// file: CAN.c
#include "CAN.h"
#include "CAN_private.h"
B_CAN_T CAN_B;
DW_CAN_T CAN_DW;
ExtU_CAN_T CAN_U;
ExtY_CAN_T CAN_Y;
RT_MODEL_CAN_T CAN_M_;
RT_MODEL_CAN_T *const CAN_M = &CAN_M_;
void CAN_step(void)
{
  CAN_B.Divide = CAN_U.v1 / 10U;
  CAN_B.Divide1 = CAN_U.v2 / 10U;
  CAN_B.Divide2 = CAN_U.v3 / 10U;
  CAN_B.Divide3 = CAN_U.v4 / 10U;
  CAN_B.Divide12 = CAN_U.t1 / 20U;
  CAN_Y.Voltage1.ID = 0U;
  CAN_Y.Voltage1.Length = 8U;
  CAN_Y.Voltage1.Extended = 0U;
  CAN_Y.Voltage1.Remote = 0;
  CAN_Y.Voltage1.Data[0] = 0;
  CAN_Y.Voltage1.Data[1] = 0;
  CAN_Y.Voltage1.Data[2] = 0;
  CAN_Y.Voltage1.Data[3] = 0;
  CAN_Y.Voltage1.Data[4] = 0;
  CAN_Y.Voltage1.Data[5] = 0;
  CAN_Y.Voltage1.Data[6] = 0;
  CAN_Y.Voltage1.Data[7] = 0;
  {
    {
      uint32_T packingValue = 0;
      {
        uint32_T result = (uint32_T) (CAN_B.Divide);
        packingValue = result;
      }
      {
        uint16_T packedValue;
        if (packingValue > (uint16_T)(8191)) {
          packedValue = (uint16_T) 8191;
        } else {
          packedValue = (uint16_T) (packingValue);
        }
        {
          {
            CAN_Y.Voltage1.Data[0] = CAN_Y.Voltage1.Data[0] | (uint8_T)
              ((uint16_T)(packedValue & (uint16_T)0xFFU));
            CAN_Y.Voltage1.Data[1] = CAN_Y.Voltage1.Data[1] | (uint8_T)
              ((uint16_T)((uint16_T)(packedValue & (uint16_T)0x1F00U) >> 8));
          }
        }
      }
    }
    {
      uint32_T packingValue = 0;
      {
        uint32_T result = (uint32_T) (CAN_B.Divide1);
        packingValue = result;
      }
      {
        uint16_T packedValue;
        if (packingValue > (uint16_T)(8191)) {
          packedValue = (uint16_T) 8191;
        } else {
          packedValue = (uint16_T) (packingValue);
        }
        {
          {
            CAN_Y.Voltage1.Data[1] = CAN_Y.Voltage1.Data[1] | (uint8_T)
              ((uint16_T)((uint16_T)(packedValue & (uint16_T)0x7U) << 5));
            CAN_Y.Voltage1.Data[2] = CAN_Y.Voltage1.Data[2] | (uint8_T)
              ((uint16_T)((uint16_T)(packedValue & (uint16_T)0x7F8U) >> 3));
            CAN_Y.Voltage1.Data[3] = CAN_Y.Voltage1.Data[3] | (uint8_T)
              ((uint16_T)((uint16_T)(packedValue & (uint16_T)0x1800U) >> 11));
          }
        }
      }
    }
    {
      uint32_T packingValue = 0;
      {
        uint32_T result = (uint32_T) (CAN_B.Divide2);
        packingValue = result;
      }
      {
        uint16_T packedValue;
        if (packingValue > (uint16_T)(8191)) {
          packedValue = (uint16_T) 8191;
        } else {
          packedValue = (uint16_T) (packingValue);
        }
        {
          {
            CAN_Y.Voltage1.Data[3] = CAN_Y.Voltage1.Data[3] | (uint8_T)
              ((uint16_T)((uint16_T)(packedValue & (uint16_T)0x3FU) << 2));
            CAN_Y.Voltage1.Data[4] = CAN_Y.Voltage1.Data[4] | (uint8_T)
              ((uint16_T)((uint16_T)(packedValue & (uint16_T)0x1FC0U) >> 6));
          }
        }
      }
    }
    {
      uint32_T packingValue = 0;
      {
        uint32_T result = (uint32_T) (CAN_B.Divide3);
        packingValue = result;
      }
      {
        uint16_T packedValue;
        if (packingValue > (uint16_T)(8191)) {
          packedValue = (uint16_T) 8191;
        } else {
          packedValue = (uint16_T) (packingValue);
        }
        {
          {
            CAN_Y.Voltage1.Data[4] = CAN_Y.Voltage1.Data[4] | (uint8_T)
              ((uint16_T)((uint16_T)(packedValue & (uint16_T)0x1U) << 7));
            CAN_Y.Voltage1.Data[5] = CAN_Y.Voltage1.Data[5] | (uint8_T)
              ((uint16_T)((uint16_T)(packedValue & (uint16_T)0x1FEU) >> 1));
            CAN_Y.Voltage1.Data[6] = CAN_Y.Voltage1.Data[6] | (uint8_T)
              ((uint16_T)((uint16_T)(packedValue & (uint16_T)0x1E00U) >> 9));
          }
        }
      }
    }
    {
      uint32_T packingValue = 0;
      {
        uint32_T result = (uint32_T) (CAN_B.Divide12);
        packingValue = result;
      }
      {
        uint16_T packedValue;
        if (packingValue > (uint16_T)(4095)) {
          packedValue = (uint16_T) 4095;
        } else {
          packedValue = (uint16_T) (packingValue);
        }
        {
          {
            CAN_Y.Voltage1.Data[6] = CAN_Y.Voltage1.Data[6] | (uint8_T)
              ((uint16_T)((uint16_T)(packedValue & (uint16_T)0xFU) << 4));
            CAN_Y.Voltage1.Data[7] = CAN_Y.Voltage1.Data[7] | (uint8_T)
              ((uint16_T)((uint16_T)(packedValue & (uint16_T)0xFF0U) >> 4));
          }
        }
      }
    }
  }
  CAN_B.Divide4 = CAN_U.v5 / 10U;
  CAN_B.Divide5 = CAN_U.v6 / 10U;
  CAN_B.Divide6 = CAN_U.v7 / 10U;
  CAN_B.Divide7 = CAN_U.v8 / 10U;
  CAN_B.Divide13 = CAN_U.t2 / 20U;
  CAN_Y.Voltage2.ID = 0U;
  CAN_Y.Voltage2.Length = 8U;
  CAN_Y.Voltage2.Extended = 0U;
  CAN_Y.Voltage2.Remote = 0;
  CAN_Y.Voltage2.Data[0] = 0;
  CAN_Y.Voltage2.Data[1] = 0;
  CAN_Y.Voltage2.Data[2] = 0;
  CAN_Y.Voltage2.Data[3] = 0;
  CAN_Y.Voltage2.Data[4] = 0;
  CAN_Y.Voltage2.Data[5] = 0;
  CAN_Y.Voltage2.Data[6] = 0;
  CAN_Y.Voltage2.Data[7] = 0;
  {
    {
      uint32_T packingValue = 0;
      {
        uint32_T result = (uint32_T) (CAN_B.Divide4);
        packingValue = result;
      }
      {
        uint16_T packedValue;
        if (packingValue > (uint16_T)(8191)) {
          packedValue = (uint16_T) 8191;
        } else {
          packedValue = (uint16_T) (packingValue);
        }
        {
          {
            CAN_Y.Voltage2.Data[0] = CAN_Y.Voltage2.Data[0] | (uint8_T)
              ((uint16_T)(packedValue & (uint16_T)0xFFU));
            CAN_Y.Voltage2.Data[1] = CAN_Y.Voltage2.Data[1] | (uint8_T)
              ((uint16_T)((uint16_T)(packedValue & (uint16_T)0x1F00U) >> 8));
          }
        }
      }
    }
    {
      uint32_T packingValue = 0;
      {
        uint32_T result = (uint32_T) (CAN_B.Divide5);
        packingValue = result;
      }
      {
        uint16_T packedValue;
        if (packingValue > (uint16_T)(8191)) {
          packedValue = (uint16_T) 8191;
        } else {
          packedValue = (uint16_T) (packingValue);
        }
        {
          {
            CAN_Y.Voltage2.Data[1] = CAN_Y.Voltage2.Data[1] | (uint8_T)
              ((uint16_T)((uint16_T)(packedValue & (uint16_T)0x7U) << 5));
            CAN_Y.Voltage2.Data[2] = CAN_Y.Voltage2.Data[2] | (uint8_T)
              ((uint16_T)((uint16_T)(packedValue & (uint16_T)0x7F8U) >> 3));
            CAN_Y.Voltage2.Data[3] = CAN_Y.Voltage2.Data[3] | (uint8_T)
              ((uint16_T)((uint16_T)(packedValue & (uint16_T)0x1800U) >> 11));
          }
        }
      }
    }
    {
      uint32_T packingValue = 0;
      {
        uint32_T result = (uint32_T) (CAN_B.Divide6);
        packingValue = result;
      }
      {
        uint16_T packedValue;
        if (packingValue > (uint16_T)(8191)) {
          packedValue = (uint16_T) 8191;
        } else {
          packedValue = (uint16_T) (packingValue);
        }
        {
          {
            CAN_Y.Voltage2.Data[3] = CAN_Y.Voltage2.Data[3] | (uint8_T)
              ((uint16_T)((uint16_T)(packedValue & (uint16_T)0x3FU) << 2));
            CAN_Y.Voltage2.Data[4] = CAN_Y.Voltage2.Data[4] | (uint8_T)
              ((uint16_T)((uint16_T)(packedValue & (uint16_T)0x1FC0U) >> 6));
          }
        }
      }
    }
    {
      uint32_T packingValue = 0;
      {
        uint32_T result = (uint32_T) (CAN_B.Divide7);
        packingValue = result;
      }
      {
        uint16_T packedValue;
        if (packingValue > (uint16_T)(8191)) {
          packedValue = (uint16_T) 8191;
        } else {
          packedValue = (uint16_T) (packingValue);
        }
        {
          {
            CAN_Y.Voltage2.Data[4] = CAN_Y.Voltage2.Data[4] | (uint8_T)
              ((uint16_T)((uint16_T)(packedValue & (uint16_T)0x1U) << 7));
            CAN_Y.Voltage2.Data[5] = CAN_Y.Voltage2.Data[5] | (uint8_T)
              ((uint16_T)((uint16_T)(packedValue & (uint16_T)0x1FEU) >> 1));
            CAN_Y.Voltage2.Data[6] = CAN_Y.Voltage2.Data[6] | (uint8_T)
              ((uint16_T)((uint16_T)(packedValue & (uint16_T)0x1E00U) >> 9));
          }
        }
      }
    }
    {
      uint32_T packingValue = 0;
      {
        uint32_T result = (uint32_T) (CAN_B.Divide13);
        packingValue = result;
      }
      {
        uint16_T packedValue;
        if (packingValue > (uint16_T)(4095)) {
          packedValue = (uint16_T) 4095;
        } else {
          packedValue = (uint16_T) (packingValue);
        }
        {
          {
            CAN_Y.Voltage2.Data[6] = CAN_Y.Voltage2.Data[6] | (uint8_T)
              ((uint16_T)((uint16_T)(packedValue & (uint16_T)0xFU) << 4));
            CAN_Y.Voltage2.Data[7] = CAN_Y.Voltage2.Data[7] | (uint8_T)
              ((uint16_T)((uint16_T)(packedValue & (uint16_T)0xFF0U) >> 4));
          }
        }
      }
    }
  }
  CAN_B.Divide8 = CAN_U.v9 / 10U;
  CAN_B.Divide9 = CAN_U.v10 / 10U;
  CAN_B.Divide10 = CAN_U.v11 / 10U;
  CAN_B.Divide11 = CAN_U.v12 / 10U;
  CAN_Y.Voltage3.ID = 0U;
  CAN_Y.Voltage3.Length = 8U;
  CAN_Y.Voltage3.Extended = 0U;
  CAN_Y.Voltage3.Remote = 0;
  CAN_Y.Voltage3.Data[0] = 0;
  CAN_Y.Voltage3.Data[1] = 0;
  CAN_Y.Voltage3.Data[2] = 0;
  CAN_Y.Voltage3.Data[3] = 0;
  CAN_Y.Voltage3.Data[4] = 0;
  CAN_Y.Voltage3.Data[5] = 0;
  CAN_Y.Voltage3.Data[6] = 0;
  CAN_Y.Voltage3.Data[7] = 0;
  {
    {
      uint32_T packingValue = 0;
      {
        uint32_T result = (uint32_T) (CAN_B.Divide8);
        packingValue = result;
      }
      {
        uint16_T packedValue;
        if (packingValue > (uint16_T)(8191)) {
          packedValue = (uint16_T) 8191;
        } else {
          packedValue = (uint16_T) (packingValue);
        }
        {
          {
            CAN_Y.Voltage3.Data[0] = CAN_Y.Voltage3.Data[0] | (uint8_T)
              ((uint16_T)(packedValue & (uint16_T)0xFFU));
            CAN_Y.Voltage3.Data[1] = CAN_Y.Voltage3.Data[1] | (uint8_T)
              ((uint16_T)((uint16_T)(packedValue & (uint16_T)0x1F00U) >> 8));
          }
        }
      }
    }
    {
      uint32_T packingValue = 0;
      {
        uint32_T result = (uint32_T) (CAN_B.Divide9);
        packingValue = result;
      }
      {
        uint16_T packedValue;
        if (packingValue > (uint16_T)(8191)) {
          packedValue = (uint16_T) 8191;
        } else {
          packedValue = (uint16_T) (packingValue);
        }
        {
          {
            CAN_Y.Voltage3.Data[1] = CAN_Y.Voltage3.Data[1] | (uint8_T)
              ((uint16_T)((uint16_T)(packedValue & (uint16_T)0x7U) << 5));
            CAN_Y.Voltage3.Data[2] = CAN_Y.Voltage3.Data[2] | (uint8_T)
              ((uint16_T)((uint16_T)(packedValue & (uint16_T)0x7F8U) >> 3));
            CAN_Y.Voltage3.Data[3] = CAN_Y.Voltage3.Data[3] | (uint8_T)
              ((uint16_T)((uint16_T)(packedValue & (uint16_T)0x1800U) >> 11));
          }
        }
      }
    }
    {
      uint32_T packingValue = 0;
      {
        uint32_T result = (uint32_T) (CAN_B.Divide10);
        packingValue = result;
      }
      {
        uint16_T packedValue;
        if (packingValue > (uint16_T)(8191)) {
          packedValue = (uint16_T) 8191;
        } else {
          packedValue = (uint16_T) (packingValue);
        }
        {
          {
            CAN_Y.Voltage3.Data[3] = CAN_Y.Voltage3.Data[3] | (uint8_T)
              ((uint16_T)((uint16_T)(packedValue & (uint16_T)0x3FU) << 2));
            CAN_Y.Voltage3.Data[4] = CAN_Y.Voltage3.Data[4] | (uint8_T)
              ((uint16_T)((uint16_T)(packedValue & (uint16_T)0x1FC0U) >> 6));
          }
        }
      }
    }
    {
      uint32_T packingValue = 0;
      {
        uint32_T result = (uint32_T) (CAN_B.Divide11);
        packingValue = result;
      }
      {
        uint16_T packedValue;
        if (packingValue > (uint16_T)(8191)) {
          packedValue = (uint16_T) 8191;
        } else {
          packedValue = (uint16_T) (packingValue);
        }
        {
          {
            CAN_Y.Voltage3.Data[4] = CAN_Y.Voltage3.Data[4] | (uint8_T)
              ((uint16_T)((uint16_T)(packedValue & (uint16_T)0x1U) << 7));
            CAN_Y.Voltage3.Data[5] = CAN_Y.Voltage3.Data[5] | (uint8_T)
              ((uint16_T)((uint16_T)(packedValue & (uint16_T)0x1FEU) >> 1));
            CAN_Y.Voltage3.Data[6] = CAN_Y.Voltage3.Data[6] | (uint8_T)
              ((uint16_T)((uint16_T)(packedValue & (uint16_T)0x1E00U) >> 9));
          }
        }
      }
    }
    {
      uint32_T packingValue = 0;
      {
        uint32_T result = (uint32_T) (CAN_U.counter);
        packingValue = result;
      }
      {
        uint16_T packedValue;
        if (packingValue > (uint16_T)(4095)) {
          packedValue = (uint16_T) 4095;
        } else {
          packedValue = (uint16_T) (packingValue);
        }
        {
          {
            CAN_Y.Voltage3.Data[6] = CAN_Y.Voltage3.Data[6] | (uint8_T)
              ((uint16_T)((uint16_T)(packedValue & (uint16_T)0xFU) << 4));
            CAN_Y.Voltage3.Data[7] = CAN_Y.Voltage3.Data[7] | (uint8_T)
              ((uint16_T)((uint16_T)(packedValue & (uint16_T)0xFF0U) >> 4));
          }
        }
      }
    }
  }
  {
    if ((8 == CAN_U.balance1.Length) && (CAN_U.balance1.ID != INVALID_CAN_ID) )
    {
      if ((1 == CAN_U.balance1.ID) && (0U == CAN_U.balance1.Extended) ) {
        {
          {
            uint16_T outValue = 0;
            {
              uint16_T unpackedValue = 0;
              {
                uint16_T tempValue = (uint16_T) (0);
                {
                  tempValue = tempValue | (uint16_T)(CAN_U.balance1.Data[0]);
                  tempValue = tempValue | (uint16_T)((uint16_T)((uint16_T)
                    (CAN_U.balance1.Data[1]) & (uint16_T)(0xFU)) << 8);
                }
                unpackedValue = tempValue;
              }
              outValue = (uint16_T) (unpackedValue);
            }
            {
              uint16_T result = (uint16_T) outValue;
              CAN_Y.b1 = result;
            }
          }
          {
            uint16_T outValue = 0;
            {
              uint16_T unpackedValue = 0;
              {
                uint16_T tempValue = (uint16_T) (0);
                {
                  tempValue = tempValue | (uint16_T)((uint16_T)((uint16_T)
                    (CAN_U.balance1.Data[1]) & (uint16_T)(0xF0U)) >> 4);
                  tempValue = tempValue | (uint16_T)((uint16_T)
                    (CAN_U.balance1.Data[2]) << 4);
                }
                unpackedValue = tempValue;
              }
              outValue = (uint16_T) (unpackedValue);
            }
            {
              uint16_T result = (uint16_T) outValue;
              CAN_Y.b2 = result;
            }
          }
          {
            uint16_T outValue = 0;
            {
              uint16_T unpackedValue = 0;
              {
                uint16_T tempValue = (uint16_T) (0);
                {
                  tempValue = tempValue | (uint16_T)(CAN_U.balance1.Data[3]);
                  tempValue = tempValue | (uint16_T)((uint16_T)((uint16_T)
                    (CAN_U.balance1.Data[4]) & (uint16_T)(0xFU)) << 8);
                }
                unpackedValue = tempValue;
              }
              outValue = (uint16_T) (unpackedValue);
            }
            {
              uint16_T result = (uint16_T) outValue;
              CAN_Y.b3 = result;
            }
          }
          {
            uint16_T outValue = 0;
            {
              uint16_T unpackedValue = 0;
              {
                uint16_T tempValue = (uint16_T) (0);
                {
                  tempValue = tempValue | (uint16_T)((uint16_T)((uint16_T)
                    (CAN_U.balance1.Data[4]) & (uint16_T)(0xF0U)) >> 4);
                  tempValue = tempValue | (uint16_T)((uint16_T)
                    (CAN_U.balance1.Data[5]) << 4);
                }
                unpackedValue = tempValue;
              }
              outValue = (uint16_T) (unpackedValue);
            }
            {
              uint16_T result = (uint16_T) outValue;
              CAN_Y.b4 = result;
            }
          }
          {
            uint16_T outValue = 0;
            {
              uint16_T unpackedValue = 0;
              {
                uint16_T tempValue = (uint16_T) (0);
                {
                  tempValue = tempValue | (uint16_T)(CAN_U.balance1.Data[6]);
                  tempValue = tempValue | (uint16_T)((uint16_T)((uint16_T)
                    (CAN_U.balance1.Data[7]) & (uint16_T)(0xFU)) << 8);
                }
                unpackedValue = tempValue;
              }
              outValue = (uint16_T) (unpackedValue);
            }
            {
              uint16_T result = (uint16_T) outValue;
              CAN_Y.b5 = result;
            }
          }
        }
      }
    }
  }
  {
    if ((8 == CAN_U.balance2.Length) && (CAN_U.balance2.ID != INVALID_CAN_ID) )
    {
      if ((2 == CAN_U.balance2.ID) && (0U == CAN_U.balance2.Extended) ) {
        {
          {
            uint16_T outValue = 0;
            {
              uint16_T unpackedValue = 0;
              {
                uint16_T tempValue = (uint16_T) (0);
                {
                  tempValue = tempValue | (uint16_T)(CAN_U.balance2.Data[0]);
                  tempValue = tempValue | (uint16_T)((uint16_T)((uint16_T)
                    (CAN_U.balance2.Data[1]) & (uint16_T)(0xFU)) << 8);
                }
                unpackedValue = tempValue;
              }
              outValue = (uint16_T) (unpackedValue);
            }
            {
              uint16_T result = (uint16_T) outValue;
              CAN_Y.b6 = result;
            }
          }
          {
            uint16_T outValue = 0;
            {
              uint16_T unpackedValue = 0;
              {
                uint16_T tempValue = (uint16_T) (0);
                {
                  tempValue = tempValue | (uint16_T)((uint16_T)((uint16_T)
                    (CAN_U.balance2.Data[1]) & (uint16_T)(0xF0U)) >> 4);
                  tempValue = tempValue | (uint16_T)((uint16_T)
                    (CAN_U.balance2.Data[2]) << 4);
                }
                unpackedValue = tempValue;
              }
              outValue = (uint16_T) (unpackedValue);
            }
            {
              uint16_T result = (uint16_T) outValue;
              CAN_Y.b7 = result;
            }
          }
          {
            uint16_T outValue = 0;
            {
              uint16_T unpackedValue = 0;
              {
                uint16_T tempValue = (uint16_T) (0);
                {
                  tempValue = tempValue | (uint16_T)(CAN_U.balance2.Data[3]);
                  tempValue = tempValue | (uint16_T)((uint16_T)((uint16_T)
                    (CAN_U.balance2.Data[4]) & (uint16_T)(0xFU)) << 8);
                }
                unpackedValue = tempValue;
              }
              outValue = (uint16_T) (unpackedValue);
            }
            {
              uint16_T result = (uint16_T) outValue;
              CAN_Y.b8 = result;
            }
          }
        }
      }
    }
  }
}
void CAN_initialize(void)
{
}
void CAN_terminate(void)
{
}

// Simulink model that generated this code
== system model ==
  v1 : Inport
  v2 : Inport
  v3 : Inport
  v4 : Inport
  v5 : Inport
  v6 : Inport
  v7 : Inport
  v8 : Inport
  v9 : Inport
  v10 : Inport
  v11 : Inport
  v12 : Inport
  t1 : Inport
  t2 : Inport
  counter : Inport
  balance2 : Inport
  balance1 : Inport
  Voltage1 : Outport  <- 1: CANPack#1
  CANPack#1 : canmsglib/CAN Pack  <- 1: Divide, 2: Divide1, 3: Divide2, 4: Divide3, 5: Divide12
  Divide : Product  Inputs=*/  <- 1: v1, 2: Constant#1
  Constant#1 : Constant  Value=10
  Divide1 : Product  Inputs=*/  <- 1: v2, 2: Constant#2
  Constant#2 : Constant  Value=10
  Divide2 : Product  Inputs=*/  <- 1: v3, 2: Constant#3
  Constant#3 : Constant  Value=10
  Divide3 : Product  Inputs=*/  <- 1: v4, 2: Constant#4
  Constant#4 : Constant  Value=10
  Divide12 : Product  Inputs=*/  <- 1: t1, 2: Constant#5
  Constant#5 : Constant  Value=20
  Voltage2 : Outport  <- 1: CANPack#2
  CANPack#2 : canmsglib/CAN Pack  <- 1: Divide4, 2: Divide5, 3: Divide6, 4: Divide7, 5: Divide13
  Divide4 : Product  Inputs=*/  <- 1: v5, 2: Constant#6
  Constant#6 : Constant  Value=10
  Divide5 : Product  Inputs=*/  <- 1: v6, 2: Constant#7
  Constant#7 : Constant  Value=10
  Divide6 : Product  Inputs=*/  <- 1: v7, 2: Constant#8
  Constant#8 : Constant  Value=10
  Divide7 : Product  Inputs=*/  <- 1: v8, 2: Constant#9
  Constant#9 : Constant  Value=10
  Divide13 : Product  Inputs=*/  <- 1: t2, 2: Constant#10
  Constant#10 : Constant  Value=20
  Voltage3 : Outport  <- 1: CANPack#3
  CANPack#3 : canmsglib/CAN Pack  <- 1: Divide8, 2: Divide9, 3: Divide10, 4: Divide11, 5: counter
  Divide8 : Product  Inputs=*/  <- 1: v9, 2: Constant#11
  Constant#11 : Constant  Value=10
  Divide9 : Product  Inputs=*/  <- 1: v10, 2: Constant#12
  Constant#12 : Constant  Value=10
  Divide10 : Product  Inputs=*/  <- 1: v11, 2: Constant#13
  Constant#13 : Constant  Value=10
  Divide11 : Product  Inputs=*/  <- 1: v12, 2: Constant#14
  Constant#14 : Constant  Value=10
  b1 : Outport  <- 1: CANUnpack#1
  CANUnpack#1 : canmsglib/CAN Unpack  <- 1: balance1
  b2 : Outport  <- 1: CANUnpack#1/2
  b3 : Outport  <- 1: CANUnpack#1/3
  b4 : Outport  <- 1: CANUnpack#1/4
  b5 : Outport  <- 1: CANUnpack#1/5
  b6 : Outport  <- 1: CANUnpack#2
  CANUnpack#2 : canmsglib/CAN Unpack  <- 1: balance2
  b7 : Outport  <- 1: CANUnpack#2/2
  b8 : Outport  <- 1: CANUnpack#2/3
